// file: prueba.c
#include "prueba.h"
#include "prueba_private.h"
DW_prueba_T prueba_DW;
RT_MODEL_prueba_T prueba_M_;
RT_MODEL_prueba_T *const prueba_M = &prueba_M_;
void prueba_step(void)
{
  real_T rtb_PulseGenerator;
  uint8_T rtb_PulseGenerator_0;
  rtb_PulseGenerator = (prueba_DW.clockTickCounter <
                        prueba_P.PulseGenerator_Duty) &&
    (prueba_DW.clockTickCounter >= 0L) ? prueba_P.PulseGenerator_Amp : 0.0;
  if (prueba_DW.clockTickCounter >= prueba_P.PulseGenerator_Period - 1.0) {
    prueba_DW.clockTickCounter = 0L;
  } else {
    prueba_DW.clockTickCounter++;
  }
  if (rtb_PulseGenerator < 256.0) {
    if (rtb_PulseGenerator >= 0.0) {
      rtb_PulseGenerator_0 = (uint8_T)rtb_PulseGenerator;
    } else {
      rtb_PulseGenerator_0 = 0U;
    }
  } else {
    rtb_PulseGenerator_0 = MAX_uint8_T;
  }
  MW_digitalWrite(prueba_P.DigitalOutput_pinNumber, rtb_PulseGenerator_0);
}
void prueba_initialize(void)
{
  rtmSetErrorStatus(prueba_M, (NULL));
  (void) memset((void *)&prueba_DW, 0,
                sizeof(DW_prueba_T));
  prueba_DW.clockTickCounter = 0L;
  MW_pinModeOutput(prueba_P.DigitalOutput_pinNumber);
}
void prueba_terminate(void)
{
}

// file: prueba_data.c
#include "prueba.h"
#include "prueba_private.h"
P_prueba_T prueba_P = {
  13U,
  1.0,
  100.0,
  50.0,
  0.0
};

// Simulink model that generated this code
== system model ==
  DigitalOutput : arduinolib/Digital Output  pinNumber=13  <- 1: PulseGenerator
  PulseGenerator : DiscretePulseGenerator  Period=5  PulseWidth=50
